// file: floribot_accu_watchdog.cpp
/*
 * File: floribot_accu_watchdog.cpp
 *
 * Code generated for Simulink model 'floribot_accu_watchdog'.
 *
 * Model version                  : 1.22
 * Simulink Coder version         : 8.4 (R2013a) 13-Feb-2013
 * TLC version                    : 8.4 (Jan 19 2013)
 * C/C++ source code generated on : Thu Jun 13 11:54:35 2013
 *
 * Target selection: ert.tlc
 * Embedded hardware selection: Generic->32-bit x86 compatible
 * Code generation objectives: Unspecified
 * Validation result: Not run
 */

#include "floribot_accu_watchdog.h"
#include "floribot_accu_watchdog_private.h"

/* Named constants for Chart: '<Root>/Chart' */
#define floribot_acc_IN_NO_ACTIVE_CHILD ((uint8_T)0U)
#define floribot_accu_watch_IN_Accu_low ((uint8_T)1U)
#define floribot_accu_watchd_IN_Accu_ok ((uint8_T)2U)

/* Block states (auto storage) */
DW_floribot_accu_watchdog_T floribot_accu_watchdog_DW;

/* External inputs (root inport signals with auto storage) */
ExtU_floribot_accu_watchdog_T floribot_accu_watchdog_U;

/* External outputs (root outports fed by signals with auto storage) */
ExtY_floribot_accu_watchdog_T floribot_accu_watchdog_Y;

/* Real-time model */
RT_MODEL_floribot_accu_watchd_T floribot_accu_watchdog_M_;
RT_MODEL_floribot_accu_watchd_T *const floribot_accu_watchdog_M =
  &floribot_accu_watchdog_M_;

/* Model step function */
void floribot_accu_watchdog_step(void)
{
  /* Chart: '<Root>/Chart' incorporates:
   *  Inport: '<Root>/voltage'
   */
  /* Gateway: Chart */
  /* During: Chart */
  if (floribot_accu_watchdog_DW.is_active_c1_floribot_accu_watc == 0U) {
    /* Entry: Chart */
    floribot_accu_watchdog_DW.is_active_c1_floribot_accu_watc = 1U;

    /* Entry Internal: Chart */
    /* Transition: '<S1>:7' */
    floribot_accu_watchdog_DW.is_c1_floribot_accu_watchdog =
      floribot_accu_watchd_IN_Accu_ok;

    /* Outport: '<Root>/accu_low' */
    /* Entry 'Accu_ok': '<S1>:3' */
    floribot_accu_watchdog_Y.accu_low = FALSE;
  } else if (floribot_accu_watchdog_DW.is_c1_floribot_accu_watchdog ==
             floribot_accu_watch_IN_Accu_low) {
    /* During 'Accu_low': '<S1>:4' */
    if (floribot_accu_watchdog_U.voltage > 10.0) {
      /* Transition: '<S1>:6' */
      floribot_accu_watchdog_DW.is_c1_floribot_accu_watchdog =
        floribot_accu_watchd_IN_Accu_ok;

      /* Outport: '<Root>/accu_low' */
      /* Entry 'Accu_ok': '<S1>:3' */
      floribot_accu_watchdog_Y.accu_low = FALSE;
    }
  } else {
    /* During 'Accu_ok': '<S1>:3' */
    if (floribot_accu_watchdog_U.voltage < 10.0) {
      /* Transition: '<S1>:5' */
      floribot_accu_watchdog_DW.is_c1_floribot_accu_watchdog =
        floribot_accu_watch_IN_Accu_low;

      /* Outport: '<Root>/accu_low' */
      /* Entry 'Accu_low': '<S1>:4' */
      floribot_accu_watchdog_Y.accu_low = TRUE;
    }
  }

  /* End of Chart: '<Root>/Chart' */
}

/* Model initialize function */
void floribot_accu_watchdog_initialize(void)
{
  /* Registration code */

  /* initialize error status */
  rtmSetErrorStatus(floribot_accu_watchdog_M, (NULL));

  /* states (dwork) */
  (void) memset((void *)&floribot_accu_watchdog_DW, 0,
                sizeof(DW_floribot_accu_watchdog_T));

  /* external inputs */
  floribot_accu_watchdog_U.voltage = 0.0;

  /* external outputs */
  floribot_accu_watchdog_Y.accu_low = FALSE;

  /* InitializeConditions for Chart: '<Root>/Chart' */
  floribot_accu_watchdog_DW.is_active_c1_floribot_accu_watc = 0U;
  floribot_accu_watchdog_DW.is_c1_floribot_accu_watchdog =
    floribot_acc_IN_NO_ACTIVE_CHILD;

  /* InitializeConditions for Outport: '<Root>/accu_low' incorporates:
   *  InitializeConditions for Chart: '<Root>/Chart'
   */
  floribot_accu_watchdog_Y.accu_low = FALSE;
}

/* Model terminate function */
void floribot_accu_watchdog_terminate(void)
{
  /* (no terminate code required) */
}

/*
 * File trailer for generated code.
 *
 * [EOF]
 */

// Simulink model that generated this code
simulink model "floribot_accu_watchdog"  (R2013a)
settings: Solver=FixedStepDiscrete  SolverMode=SingleTasking  StartTime=0.0  StopTime=inf  FixedStep=0.1  RelTol=1e-3  SampleTimeConstraint=STIndependent

== system floribot_accu_watchdog ==
  voltage : Inport
  Chart : Stateflow chart  TreatAsAtomicUnit=on
  accu_low : Outport
  wires:
  voltage/1 -> Chart/1(voltage)
  Chart/1(accu_low) -> accu_low/1

== stateflow chart floribot_accu_watchdog/Chart ==
  state Accu_ok
    accu_low = false;
  state Accu_low
    accu_low = true;
  (default) -> Accu_ok
  Accu_ok -> Accu_low : [voltage < 10]
  Accu_low -> Accu_ok : [voltage > 10]
  data: voltage input double; accu_low output boolean
